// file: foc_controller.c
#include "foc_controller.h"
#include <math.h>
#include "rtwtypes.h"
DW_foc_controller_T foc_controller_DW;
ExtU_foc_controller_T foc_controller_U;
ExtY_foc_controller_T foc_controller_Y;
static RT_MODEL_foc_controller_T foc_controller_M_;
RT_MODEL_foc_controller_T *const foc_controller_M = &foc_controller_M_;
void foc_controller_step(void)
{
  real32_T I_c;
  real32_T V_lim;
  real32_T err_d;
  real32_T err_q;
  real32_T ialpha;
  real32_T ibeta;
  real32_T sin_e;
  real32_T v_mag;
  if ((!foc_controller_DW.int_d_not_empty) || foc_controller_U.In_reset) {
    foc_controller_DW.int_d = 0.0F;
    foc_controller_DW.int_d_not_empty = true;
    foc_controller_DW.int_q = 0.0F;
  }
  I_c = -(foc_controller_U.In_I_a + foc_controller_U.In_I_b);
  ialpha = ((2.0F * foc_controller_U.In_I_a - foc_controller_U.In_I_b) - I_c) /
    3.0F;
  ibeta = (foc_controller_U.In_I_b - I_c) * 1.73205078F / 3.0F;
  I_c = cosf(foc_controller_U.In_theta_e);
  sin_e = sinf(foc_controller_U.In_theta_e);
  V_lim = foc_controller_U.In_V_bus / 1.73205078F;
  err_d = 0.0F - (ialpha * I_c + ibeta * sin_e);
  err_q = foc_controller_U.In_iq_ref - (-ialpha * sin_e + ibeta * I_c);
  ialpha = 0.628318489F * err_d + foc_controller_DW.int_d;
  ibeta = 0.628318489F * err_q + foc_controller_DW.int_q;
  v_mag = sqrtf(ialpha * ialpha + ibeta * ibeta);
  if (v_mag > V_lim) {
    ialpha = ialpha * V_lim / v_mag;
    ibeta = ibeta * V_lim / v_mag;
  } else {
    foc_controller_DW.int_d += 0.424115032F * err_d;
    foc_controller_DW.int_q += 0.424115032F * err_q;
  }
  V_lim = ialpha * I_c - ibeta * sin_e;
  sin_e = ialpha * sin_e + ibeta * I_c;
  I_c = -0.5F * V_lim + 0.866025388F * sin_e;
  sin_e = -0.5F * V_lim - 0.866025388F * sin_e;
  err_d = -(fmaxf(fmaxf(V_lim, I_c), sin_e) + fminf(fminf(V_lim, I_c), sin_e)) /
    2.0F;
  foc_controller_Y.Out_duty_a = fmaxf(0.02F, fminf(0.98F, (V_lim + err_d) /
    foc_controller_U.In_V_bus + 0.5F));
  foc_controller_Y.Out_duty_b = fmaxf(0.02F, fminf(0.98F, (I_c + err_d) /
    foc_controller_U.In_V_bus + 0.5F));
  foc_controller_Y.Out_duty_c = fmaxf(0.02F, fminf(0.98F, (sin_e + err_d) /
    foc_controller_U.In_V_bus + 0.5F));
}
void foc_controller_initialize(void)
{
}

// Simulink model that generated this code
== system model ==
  In_I_a : Inport
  In_I_b : Inport
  In_theta_e : Inport
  In_iq_ref : Inport
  In_V_bus : Inport
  In_reset : Inport
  Out_duty_a : Outport  <- 1: MATLABFunction#1
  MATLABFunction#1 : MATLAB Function  <- 1: In_I_a, 2: In_I_b, 3: In_theta_e, 4: In_iq_ref, 5: In_V_bus, 6: In_reset
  Out_duty_b : Outport  <- 1: MATLABFunction#1/2
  Out_duty_c : Outport  <- 1: MATLABFunction#1/3
== matlab function MATLABFunction#1 ==
function [duty_a, duty_b, duty_c] = foc_core(I_a, I_b, theta_e, iq_ref, V_bus, Ts_ctrl, duty_min, duty_max, reset, Kp_d, Ki_d, Kp_q, Ki_q)
%#codegen
% FOC 电流环控制器 — 对齐固件 foc_interface.h
% Parameters (从 foc_params.m): Kp_d, Ki_d, Kp_q, Ki_q, Ts_ctrl, duty_min, duty_max

persistent int_d int_q
if isempty(int_d) || reset
    int_d = single(0);
    int_q = single(0);
end

id_ref = single(0);  % SPM: id=0 内部固定

% 1. IW 软件计算
I_c = -(I_a + I_b);

% 2. Clarke (等幅值 2/3)
ialpha = (2*I_a - I_b - I_c) / 3;
ibeta  = (sqrt(single(3)) * (I_b - I_c)) / 3;

% 3. Park
cos_e = cos(theta_e);
sin_e = sin(theta_e);
id_fb =  ialpha * cos_e + ibeta * sin_e;
iq_fb = -ialpha * sin_e + ibeta * cos_e;

% 4. PI (抗积分饱和)
V_lim = V_bus / sqrt(single(3));
err_d = id_ref - id_fb;
err_q = iq_ref - iq_fb;

vd_star = Kp_d * err_d + int_d;
vq_star = Kp_q * err_q + int_q;

v_mag = sqrt(vd_star*vd_star + vq_star*vq_star);
if v_mag > V_lim
    vd_star = vd_star * V_lim / v_mag;
    vq_star = vq_star * V_lim / v_mag;
else
    int_d = int_d + Ki_d * Ts_ctrl * err_d;
    int_q = int_q + Ki_q * Ts_ctrl * err_q;
end

% 5. 逆 Park
valpha = vd_star * cos_e - vq_star * sin_e;
vbeta  = vd_star * sin_e + vq_star * cos_e;

% 6. SVPWM (中性点注入)
va = valpha;
vb = -single(0.5)*valpha + (sqrt(single(3))/2)*vbeta;
vc = -single(0.5)*valpha - (sqrt(single(3))/2)*vbeta;
v_off = -(max(max(va,vb),vc) + min(min(va,vb),vc)) / 2;
va = va + v_off; vb = vb + v_off; vc = vc + v_off;

duty_a = max(duty_min, min(duty_max, va/V_bus + single(0.5)));
duty_b = max(duty_min, min(duty_max, vb/V_bus + single(0.5)));
duty_c = max(duty_min, min(duty_max, vc/V_bus + single(0.5)));
